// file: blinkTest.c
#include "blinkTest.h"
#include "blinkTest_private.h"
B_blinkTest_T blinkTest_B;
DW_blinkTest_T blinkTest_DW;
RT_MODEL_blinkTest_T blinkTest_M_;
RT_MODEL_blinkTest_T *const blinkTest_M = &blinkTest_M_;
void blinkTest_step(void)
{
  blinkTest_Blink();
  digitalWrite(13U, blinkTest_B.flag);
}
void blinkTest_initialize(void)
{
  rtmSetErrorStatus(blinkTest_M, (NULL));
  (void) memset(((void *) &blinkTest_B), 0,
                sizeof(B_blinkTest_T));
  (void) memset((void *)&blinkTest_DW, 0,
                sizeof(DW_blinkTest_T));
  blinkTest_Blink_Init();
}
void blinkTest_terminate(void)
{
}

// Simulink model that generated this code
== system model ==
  Stateflowchart#1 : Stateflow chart  <- 1: Constant#1, 2: Blink
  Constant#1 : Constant  Value=13
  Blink : Subsystem
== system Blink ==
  Outport#1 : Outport  <- 1: Stateflowchart#2
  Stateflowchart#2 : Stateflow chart
== stateflow chart Chart ==
  (default) -> (junction 1)
  (junction 1) -> (junction 3) : {
      | digitalWrite(pin, value);
      | }
  data: pin input uint8; value input boolean

== stateflow chart Chart ==
  state on
    en:
    flag = true;
  state off
    en:
    flag = false;
  (default) -> off
  on -> off : [after(1000,tick)]
  off -> on : [after(1000,tick)]
  data: flag output boolean
